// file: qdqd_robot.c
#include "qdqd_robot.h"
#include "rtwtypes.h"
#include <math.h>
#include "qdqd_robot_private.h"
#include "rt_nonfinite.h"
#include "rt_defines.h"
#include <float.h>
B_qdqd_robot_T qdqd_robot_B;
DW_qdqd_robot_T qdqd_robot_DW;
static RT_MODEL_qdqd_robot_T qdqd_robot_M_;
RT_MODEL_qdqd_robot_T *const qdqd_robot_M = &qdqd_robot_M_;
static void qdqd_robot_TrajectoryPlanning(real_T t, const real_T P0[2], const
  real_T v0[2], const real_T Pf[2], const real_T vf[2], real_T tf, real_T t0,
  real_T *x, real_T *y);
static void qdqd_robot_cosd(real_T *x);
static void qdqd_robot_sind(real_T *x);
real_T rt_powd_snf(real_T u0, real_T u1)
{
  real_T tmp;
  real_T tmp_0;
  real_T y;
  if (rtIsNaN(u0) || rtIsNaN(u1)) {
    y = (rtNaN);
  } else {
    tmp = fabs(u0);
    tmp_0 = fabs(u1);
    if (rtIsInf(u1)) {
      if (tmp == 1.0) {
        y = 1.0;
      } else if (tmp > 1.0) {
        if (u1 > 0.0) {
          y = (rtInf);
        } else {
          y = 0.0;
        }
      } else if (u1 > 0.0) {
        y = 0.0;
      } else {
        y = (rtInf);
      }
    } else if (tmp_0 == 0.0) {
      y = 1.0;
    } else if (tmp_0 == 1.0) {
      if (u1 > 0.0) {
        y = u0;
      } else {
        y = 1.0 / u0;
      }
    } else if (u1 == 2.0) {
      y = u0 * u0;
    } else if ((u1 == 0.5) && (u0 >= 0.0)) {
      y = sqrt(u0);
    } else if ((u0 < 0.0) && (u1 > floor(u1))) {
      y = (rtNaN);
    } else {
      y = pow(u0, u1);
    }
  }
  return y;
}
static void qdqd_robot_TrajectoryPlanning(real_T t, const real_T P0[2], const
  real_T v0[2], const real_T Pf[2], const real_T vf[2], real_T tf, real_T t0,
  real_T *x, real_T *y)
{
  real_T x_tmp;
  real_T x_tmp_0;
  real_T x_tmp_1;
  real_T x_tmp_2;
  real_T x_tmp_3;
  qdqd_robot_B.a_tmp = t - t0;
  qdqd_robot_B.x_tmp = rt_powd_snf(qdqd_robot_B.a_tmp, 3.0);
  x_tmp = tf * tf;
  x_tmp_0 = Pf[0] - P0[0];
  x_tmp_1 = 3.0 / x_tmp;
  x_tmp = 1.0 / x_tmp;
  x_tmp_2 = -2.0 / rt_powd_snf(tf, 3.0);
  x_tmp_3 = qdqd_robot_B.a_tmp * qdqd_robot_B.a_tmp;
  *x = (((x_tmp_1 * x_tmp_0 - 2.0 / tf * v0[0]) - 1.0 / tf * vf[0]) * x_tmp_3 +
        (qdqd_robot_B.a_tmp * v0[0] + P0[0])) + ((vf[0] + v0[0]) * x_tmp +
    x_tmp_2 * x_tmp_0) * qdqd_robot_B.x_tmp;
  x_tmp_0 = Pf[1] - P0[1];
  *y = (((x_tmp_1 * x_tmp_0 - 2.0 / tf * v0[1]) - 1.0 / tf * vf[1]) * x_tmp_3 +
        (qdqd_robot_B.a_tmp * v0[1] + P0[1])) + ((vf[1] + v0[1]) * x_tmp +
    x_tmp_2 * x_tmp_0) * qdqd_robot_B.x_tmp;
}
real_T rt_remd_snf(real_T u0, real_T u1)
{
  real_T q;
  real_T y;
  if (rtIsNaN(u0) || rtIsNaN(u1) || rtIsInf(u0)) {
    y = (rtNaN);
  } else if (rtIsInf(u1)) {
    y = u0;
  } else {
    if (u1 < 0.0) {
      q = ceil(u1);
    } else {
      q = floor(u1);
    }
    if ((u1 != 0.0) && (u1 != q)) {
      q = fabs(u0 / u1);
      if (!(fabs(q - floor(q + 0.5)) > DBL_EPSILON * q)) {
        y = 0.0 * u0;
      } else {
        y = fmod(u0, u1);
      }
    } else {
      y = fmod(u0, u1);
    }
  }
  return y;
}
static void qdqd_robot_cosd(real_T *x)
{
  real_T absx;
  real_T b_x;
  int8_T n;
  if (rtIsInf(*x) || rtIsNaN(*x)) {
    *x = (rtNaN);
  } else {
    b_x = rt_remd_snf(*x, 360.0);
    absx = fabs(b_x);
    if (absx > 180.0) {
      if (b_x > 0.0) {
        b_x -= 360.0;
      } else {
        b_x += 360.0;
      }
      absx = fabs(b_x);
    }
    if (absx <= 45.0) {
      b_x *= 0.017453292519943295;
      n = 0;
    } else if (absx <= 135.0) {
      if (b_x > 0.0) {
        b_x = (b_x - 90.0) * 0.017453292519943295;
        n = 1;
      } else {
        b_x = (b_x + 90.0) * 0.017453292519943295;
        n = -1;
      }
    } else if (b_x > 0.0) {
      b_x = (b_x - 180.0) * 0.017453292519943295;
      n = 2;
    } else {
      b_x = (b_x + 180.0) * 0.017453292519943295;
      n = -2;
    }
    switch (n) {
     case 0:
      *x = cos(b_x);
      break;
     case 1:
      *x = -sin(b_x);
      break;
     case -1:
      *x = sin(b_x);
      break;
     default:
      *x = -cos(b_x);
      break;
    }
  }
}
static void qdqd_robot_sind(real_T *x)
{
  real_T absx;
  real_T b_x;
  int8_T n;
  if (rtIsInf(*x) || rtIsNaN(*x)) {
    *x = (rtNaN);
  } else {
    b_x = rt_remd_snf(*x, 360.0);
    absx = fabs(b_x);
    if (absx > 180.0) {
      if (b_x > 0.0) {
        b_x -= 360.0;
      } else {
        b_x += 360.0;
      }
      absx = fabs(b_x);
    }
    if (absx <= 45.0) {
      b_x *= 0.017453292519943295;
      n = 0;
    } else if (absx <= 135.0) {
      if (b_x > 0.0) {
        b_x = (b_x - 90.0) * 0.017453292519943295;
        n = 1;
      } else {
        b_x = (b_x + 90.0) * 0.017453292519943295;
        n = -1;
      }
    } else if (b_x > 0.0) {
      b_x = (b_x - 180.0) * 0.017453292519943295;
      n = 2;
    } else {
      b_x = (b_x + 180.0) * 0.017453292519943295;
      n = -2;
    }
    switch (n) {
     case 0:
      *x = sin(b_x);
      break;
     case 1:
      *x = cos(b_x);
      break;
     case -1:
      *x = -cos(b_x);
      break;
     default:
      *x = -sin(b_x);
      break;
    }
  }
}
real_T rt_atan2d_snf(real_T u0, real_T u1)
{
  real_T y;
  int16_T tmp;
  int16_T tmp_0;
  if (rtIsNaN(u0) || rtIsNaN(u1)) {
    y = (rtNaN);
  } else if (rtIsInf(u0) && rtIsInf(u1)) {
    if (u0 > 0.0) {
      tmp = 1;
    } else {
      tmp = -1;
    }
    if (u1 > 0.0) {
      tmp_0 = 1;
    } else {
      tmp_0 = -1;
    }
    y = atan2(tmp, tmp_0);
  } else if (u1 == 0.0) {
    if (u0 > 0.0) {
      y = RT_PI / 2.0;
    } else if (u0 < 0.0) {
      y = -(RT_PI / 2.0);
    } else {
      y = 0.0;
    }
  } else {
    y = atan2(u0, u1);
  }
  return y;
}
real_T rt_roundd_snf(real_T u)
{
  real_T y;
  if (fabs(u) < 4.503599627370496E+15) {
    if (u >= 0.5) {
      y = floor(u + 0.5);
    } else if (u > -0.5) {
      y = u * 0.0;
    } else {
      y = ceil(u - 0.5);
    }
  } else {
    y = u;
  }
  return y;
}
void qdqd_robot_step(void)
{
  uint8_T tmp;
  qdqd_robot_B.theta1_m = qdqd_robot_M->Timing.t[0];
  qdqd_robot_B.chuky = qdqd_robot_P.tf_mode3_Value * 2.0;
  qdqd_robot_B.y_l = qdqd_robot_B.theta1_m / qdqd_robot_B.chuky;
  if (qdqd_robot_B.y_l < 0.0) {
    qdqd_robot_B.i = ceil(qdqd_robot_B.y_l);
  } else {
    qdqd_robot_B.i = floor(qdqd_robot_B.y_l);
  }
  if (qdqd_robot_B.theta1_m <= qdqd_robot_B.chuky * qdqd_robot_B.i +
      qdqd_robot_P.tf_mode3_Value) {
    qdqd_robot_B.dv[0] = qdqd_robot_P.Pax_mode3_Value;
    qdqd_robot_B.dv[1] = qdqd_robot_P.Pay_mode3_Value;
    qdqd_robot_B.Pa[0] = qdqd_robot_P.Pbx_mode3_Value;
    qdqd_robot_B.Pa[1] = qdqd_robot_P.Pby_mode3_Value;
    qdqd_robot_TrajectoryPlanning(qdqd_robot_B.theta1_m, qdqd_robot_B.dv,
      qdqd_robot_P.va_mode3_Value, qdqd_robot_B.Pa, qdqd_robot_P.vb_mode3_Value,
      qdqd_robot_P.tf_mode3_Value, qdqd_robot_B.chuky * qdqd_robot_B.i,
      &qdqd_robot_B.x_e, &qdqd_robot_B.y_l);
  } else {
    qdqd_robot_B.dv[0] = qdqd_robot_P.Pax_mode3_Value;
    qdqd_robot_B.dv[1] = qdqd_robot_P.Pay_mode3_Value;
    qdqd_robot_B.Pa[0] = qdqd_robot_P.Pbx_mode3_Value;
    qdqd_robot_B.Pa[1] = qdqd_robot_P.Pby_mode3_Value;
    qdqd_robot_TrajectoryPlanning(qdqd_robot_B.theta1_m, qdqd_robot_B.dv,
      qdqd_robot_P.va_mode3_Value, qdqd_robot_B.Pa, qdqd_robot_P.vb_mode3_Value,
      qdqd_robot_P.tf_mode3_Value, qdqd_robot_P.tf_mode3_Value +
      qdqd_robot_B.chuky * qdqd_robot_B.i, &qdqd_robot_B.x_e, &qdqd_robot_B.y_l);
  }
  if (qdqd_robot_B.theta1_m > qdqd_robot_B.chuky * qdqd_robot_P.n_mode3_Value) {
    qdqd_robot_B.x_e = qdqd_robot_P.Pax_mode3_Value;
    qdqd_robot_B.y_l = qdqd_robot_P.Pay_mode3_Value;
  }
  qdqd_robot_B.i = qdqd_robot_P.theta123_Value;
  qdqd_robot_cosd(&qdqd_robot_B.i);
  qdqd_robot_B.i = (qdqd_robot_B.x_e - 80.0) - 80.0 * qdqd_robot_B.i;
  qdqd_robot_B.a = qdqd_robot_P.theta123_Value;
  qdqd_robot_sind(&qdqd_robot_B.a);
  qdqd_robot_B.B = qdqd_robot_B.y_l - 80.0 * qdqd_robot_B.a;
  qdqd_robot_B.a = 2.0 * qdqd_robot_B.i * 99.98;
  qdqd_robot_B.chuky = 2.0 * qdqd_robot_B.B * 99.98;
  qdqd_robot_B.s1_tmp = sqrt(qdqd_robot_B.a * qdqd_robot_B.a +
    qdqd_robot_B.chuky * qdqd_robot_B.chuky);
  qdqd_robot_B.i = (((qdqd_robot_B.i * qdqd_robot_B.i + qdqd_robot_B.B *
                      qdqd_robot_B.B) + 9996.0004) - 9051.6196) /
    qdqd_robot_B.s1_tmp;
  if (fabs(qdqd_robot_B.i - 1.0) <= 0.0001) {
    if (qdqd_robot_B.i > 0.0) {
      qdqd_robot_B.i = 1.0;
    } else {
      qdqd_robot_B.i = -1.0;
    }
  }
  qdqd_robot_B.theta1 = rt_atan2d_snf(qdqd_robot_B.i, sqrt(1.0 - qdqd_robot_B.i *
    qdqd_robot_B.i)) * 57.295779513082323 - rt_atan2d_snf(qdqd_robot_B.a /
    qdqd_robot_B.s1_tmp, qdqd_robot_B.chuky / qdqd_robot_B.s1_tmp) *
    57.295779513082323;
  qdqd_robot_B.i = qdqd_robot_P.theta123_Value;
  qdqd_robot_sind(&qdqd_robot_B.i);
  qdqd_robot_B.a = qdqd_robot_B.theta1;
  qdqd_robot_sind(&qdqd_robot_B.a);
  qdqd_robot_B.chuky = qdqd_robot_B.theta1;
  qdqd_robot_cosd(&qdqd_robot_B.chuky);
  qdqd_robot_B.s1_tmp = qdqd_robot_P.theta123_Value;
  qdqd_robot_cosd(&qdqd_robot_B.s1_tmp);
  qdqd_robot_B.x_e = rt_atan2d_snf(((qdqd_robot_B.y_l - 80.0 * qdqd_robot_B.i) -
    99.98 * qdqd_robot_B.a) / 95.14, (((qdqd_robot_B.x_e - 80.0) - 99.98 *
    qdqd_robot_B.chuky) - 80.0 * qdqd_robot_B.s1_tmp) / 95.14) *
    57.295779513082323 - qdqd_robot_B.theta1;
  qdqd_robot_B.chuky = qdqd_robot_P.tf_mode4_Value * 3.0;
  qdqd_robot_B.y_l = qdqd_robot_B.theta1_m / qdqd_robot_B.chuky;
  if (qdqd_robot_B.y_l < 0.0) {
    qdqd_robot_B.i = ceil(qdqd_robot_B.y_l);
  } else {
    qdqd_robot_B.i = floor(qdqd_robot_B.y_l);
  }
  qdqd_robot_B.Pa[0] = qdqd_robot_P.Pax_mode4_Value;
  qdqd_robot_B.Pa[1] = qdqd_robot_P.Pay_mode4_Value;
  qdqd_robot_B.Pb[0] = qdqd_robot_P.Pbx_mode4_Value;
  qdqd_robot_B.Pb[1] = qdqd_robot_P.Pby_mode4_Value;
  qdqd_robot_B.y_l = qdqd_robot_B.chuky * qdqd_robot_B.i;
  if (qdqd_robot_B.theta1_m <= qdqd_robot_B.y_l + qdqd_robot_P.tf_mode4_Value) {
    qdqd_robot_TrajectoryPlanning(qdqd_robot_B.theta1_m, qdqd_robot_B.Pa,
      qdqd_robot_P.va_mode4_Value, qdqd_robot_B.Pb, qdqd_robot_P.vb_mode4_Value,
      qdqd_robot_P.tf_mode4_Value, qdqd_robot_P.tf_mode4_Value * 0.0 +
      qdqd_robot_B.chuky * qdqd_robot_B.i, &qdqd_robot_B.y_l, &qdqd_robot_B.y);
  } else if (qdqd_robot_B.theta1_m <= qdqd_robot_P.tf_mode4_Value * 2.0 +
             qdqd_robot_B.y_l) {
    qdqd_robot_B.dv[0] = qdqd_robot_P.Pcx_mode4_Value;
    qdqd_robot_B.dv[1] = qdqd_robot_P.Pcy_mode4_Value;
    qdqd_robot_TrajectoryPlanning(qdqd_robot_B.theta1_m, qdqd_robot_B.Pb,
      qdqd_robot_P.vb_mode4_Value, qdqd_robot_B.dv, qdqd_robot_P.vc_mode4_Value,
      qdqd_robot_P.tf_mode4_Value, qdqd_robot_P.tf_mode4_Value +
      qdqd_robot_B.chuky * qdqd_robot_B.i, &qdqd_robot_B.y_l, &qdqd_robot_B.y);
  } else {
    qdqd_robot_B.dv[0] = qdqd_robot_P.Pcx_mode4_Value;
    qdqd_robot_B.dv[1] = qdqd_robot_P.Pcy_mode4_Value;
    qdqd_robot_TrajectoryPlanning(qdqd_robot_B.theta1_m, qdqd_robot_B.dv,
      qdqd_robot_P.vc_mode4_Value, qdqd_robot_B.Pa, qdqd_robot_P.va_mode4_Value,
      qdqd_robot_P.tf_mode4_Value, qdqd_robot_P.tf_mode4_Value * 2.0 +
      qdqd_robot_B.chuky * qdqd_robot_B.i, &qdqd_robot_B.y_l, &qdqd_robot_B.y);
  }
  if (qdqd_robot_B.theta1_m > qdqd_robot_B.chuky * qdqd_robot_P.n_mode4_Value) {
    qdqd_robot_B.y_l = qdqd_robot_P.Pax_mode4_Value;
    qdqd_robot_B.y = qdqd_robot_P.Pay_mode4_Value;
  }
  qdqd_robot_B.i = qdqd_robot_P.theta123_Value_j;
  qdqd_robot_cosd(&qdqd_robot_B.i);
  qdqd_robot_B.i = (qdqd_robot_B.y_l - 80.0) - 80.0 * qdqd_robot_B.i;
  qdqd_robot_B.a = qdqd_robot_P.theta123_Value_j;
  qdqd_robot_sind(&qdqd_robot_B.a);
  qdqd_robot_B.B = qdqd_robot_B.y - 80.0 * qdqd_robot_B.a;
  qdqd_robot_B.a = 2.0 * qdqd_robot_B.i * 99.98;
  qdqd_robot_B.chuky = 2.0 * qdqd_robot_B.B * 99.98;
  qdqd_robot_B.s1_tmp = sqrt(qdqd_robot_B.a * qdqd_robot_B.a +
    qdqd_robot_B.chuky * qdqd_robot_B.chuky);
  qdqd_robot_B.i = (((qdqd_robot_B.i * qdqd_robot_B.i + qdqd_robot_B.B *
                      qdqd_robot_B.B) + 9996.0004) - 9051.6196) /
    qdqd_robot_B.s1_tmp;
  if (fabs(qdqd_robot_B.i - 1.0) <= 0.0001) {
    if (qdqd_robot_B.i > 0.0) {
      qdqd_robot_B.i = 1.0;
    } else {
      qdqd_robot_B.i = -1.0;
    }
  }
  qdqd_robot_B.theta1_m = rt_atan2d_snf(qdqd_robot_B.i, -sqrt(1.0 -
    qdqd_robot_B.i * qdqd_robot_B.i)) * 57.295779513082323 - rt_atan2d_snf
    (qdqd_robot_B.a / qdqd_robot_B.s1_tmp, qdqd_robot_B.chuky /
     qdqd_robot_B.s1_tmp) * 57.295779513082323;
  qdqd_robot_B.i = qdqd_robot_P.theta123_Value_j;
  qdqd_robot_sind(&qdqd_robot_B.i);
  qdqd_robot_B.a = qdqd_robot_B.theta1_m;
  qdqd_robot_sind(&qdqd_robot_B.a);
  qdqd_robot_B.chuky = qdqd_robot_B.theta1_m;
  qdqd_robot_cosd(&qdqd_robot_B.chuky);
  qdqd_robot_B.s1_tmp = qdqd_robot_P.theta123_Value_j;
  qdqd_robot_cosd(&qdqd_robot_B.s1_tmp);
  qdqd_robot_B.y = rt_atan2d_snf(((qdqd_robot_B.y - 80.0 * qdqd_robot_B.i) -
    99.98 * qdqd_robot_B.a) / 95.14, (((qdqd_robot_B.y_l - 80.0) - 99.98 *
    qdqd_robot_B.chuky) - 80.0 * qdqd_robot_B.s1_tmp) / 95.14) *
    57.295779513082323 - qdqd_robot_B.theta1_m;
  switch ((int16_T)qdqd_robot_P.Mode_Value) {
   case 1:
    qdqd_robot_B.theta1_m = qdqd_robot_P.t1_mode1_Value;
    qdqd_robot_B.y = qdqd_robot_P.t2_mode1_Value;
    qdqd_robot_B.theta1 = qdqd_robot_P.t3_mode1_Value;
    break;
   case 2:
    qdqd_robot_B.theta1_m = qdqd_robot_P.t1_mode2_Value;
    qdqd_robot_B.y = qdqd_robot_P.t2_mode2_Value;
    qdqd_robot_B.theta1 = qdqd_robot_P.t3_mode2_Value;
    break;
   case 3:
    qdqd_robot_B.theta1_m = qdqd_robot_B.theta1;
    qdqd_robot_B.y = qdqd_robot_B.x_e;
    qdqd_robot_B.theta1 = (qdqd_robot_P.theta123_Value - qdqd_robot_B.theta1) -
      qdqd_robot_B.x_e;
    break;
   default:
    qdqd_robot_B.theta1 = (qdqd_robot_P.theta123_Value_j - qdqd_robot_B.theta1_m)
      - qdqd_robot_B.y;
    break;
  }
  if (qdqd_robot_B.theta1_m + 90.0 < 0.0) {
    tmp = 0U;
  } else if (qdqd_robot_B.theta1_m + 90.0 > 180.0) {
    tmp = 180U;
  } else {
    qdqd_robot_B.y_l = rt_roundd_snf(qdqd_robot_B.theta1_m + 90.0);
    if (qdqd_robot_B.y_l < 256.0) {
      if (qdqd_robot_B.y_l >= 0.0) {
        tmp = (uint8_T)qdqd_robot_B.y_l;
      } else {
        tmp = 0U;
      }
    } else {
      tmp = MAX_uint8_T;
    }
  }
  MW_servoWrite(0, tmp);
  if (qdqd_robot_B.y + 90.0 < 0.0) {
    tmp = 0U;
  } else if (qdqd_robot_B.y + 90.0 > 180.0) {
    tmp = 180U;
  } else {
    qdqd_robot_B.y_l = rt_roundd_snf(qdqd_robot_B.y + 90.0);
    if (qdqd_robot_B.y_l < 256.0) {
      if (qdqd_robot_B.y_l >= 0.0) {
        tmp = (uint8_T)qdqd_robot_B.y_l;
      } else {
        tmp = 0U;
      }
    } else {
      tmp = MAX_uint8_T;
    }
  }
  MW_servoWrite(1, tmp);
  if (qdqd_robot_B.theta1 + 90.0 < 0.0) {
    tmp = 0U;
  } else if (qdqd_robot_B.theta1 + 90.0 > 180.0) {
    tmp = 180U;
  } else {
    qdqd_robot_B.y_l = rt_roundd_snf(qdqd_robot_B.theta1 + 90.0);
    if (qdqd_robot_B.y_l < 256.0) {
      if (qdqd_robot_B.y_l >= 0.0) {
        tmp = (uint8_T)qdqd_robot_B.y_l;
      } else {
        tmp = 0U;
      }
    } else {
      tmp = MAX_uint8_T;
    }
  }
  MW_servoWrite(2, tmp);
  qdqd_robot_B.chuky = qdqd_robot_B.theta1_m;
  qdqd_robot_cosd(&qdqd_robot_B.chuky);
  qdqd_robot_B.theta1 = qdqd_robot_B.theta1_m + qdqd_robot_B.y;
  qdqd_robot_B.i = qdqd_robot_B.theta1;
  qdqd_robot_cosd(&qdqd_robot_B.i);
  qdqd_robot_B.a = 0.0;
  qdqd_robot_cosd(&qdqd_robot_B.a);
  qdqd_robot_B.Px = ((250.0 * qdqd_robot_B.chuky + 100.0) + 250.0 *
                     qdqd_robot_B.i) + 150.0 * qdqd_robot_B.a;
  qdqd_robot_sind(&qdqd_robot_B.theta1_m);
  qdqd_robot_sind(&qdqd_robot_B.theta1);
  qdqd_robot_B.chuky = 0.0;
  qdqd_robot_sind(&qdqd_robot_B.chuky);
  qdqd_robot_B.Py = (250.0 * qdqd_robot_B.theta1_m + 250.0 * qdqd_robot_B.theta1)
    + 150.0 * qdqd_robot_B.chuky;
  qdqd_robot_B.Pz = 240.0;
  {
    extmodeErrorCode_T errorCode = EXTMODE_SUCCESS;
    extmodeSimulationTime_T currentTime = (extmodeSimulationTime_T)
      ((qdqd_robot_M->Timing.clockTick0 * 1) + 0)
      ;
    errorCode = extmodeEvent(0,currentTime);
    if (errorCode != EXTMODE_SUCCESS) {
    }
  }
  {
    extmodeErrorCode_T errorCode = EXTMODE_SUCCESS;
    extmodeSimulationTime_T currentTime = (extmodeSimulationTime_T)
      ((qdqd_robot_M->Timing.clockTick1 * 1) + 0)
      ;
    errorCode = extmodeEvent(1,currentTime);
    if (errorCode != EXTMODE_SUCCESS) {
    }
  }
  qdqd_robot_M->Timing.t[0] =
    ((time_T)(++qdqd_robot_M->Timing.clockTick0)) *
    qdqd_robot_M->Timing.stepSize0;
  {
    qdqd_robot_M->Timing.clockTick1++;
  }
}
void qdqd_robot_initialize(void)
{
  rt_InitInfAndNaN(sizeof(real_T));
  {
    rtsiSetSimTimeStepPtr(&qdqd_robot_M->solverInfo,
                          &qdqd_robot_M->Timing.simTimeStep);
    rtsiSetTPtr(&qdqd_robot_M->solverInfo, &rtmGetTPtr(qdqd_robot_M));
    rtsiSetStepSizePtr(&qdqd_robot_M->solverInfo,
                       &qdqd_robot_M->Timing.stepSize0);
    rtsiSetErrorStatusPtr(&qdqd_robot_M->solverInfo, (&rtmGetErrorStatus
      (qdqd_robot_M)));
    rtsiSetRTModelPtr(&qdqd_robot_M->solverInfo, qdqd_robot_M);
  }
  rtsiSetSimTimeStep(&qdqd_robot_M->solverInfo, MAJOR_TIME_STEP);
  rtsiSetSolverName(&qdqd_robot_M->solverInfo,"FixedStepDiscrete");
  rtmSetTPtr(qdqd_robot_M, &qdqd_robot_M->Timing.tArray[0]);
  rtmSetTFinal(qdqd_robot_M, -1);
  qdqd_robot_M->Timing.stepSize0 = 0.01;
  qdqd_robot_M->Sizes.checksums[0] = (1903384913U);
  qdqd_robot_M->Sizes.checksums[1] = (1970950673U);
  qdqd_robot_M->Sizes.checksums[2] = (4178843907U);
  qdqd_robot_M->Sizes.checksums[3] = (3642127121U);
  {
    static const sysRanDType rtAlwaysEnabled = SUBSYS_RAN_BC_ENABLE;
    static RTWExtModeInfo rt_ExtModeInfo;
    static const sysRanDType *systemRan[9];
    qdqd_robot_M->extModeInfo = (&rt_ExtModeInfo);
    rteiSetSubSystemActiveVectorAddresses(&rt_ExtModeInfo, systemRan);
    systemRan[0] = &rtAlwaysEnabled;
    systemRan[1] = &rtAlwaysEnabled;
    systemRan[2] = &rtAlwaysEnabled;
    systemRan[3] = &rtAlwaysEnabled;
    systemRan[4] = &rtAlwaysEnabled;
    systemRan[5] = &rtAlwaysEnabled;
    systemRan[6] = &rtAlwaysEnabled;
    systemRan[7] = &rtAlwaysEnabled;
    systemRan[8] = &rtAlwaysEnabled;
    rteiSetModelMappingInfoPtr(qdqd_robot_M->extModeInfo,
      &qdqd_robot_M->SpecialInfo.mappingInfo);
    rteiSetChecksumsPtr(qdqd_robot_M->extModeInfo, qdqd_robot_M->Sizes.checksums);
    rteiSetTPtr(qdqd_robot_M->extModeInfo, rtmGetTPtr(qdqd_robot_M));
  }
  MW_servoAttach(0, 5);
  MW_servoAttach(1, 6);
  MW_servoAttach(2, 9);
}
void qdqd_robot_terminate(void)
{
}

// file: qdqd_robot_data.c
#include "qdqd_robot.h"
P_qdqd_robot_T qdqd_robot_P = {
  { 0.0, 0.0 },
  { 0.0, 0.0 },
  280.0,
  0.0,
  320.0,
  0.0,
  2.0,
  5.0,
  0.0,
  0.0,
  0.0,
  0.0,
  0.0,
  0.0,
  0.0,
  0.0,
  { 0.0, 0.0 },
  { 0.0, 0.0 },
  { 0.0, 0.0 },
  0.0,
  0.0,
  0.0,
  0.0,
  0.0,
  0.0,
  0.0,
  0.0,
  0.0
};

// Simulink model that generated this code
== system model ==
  MATLABFunction#1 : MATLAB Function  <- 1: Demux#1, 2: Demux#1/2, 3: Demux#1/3
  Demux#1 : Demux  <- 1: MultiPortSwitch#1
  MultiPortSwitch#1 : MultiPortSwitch  Inputs=4  <- 1: Mode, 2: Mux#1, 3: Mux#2, 4: MATLABFunction#2, 5: MATLABFunction#3
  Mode : Constant  Value=0
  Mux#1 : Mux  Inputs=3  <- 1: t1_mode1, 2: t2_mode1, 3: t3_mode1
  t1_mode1 : Constant  Value=0
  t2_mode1 : Constant  Value=0
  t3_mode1 : Constant  Value=0
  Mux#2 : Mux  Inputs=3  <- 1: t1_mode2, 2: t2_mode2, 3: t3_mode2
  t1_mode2 : Constant  Value=0
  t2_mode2 : Constant  Value=0
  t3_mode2 : Constant  Value=0
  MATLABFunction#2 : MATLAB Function  <- 1: MATLABFunction#4, 2: MATLABFunction#4/2, 3: theta123
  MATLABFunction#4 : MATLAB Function  <- 1: Clock#1, 2: Pax_mode3, 3: Pay_mode3, 4: va_mode3, 5: Pbx_mode3, 6: Pby_mode3, 7: vb_mode3, 8: tf_mode3, 9: n_mode3
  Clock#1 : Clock
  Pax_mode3 : Constant  Value=280
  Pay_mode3 : Constant  Value=0
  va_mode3 : Constant  Value=[0 0]
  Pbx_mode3 : Constant  Value=320
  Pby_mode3 : Constant  Value=0
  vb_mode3 : Constant  Value=[0 0]
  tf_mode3 : Constant  Value=2
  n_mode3 : Constant  Value=5
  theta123 : Constant  Value=0
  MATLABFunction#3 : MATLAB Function  <- 1: MATLABFunction#5, 2: MATLABFunction#5/2, 3: Constant#1
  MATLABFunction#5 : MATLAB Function  <- 1: Clock#2, 2: Pax_mode4, 3: Pay_mode4, 4: va_mode4, 5: Pbx_mode4, 6: Pby_mode4, 7: vb_mode4, 8: Pcx_mode4, 9: Pcy_mode4, 10: vc_mode4, 11: tf_mode4, 12: n_mode4
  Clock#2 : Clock
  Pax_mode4 : Constant  Value=0
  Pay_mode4 : Constant  Value=0
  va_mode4 : Constant  Value=[0 0]
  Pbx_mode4 : Constant  Value=0
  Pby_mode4 : Constant  Value=0
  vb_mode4 : Constant  Value=[0 0]
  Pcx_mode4 : Constant  Value=0
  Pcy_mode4 : Constant  Value=0
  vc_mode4 : Constant  Value=[0 0]
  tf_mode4 : Constant  Value=0
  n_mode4 : Constant  Value=0
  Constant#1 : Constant  Value=0
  ContinuousServoWrite#1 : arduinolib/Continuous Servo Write  pinNumber=5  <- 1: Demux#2
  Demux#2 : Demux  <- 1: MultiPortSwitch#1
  ContinuousServoWrite#2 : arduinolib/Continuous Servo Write  pinNumber=6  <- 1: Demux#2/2
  ContinuousServoWrite#3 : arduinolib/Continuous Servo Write  pinNumber=9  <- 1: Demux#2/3
== matlab function MATLABFunction#2 ==
function goc  = DHNghich(Px, Py, theta123)
     l0 = 80;
     l1 = 99.98;
     l2 = 95.14;
     l3 = 80;
     d1 = 122.4;
     d2 = 22.4;
     d3 = 18.85;

     % Tinh theta1 
     A = Px - l0 - l3*cosd(theta123);
     B = Py - l3*sind(theta123);
     a = 2*A*l1;
     b = 2*B*l1;
     d = A^2 + B^2 + l1^2 - l2^2;
     anpha = atan2d(a/sqrt(a^2+b^2), b/sqrt(a^2+b^2));
     s1 = d/sqrt(a^2+b^2);
     if(abs(s1 - 1) <= 0.0001)
            if(s1 > 0)
                 s1 = 1;
            else s1 = -1;
            end
     end
     c1 = sqrt(1 - s1^2);
     theta1 = atan2d(s1, c1) - anpha;
     % Tinh theta2
     s2 = (Py - l3*sind(theta123) - l1*sind(theta1)) / l2;
     c2 = (Px - l0 - l1*cosd(theta1) - l3*cosd(theta123))/l2;
     theta2 = atan2d(s2,c2) - theta1;
     % Tinh theta3
    theta3 = theta123 - theta1 - theta2;
    goc = [theta1; theta2; theta3];
end

== matlab function MATLAB Function ==
function [x, y] = QHQD2D(t, Pax, Pay, va, Pbx, Pby, vb, tf, solan)

    function [x, y] = TrajectoryPlanning(t, P0, v0, Pf, vf, tf, t0)
        a10 = P0(1);
        a20 = P0(2);
        a11 = v0(1);
        a21 = v0(2);  
    
        a12 = 3 / tf^2 * (Pf(1) - P0(1)) - 2 / tf * v0(1) - 1 / tf * vf(1);
        a22 = 3 / tf^2 * (Pf(2) - P0(2)) - 2 / tf * v0(2) - 1 / tf * vf(2);
        a13 = -2 / tf^3 * (Pf(1) - P0(1)) + 1 / tf^2 * (vf(1) + v0(1));
        a23 = -2 / tf^3 * (Pf(2) - P0(2)) + 1 / tf^2 * (vf(2) + v0(2));
    
        x = a10 + a11 *(t - t0) + a12 * (t - t0)^2 + a13*(t - t0)^3;
        y = a20 + a21 *(t - t0) + a22 * (t - t0)^2 + a23*(t - t0)^3;
    end

    chuky = tf*2;
    i = fix(t/chuky);
    Pa = [Pax Pay];
    Pb = [Pbx Pby];
    if(t <= (tf + chuky*i))
        [x, y] = TrajectoryPlanning(t, Pa, va, Pb, vb, tf, 0 + chuky * i);
    else
        [x, y] = TrajectoryPlanning(t, Pa, va, Pb, vb, tf, tf + chuky * i);
    end
    if(t > chuky*solan)
         x = Pax;
         y = Pay;
    end
end

== matlab function MATLAB Function ==
function [x, y] = QHQD3D(t, Pax, Pay, va, Pbx, Pby, vb, Pcx, Pcy, vc, tf, solan) 
    function [x, y, z] = TrajectoryPlanning(t, P0, v0, Pf, vf, tf, t0)
        a10 = P0(1);
        a20 = P0(2);
        a11 = v0(1);
        a21 = v0(2);  
    
        a12 = 3 / tf^2 * (Pf(1) - P0(1)) - 2 / tf * v0(1) - 1 / tf * vf(1);
        a22 = 3 / tf^2 * (Pf(2) - P0(2)) - 2 / tf * v0(2) - 1 / tf * vf(2);
        a13 = -2 / tf^3 * (Pf(1) - P0(1)) + 1 / tf^2 * (vf(1) + v0(1));
        a23 = -2 / tf^3 * (Pf(2) - P0(2)) + 1 / tf^2 * (vf(2) + v0(2));
    
        x = a10 + a11 *(t - t0) + a12 * (t - t0)^2 + a13*(t - t0)^3;
        y = a20 + a21 *(t - t0) + a22 * (t - t0)^2 + a23*(t - t0)^3;
        z = 0;
    end
    chuky = tf*3;
    i = fix(t/chuky);
    Pa = [Pax Pay];
    Pb = [Pbx Pby];
    Pc = [Pcx Pcy];
    if(t <= (tf + chuky*i))
        [x, y] = TrajectoryPlanning(t, Pa, va, Pb, vb, tf, tf*0 + chuky * i);
    elseif(t <= (tf*2 + chuky*i))
        [x, y] = TrajectoryPlanning(t, Pb, vb, Pc, vc, tf, tf*1 + chuky * i);
    else
        [x, y] = TrajectoryPlanning(t, Pc, vc, Pa, va, tf, tf*2 + chuky * i);
    end
    if(t > chuky*solan)
         x = Pax;
         y = Pay;
    end
end

== matlab function MATLABFunction#3 ==
function goc  = DHNghich(Px, Py, theta123)
    l0 = 80;
     l1 = 99.98;
     l2 = 95.14;
     l3 = 80;
     d1 = 122.4;
     d2 = 22.4;
     d3 = 18.85;

     % Tinh theta1 
     A = Px - l0 - l3*cosd(theta123);
     B = Py - l3*sind(theta123);
     a = 2*A*l1;
     b = 2*B*l1;
     d = A^2 + B^2 + l1^2 - l2^2;
     anpha = atan2d(a/sqrt(a^2+b^2), b/sqrt(a^2+b^2));
     s1 = d/sqrt(a^2+b^2);
     if(abs(s1 - 1) <= 0.0001)
            if(s1 > 0)
                 s1 = 1;
            else s1 = -1;
            end
     end
     c1 = sqrt(1 - s1^2);
     theta1 = atan2d(s1, -c1) - anpha;
     % Tinh theta2
     s2 = (Py - l3*sind(theta123) - l1*sind(theta1)) / l2;
     c2 = (Px - l0 - l1*cosd(theta1) - l3*cosd(theta123))/l2;
     theta2 = atan2d(s2,c2) - theta1;
     % Tinh theta3
    theta3 = theta123 - theta1 - theta2;
    goc = [theta1; theta2; theta3];
end

== matlab function MATLABFunction#1 ==
function [Px, Py, Pz] = DHThuan(theta1, theta2, theta3)
    l1 = 100;
    l2 = 250;
    l3 = 250;
    l4 = 150;
    d1 = 30;
    d2 = 30;
    d3 = 30;
    l0 = 150;

    theta123= 0;

    Px = l1 + l2*cosd(theta1) + l3*cosd(theta1 + theta2) + l4*cosd(theta123);
    Py = l2*sind(theta1) + l3*sind(theta1 + theta2) + l4*sind(theta123);
    Pz = l0 + d1 + d2 + d3;
end
